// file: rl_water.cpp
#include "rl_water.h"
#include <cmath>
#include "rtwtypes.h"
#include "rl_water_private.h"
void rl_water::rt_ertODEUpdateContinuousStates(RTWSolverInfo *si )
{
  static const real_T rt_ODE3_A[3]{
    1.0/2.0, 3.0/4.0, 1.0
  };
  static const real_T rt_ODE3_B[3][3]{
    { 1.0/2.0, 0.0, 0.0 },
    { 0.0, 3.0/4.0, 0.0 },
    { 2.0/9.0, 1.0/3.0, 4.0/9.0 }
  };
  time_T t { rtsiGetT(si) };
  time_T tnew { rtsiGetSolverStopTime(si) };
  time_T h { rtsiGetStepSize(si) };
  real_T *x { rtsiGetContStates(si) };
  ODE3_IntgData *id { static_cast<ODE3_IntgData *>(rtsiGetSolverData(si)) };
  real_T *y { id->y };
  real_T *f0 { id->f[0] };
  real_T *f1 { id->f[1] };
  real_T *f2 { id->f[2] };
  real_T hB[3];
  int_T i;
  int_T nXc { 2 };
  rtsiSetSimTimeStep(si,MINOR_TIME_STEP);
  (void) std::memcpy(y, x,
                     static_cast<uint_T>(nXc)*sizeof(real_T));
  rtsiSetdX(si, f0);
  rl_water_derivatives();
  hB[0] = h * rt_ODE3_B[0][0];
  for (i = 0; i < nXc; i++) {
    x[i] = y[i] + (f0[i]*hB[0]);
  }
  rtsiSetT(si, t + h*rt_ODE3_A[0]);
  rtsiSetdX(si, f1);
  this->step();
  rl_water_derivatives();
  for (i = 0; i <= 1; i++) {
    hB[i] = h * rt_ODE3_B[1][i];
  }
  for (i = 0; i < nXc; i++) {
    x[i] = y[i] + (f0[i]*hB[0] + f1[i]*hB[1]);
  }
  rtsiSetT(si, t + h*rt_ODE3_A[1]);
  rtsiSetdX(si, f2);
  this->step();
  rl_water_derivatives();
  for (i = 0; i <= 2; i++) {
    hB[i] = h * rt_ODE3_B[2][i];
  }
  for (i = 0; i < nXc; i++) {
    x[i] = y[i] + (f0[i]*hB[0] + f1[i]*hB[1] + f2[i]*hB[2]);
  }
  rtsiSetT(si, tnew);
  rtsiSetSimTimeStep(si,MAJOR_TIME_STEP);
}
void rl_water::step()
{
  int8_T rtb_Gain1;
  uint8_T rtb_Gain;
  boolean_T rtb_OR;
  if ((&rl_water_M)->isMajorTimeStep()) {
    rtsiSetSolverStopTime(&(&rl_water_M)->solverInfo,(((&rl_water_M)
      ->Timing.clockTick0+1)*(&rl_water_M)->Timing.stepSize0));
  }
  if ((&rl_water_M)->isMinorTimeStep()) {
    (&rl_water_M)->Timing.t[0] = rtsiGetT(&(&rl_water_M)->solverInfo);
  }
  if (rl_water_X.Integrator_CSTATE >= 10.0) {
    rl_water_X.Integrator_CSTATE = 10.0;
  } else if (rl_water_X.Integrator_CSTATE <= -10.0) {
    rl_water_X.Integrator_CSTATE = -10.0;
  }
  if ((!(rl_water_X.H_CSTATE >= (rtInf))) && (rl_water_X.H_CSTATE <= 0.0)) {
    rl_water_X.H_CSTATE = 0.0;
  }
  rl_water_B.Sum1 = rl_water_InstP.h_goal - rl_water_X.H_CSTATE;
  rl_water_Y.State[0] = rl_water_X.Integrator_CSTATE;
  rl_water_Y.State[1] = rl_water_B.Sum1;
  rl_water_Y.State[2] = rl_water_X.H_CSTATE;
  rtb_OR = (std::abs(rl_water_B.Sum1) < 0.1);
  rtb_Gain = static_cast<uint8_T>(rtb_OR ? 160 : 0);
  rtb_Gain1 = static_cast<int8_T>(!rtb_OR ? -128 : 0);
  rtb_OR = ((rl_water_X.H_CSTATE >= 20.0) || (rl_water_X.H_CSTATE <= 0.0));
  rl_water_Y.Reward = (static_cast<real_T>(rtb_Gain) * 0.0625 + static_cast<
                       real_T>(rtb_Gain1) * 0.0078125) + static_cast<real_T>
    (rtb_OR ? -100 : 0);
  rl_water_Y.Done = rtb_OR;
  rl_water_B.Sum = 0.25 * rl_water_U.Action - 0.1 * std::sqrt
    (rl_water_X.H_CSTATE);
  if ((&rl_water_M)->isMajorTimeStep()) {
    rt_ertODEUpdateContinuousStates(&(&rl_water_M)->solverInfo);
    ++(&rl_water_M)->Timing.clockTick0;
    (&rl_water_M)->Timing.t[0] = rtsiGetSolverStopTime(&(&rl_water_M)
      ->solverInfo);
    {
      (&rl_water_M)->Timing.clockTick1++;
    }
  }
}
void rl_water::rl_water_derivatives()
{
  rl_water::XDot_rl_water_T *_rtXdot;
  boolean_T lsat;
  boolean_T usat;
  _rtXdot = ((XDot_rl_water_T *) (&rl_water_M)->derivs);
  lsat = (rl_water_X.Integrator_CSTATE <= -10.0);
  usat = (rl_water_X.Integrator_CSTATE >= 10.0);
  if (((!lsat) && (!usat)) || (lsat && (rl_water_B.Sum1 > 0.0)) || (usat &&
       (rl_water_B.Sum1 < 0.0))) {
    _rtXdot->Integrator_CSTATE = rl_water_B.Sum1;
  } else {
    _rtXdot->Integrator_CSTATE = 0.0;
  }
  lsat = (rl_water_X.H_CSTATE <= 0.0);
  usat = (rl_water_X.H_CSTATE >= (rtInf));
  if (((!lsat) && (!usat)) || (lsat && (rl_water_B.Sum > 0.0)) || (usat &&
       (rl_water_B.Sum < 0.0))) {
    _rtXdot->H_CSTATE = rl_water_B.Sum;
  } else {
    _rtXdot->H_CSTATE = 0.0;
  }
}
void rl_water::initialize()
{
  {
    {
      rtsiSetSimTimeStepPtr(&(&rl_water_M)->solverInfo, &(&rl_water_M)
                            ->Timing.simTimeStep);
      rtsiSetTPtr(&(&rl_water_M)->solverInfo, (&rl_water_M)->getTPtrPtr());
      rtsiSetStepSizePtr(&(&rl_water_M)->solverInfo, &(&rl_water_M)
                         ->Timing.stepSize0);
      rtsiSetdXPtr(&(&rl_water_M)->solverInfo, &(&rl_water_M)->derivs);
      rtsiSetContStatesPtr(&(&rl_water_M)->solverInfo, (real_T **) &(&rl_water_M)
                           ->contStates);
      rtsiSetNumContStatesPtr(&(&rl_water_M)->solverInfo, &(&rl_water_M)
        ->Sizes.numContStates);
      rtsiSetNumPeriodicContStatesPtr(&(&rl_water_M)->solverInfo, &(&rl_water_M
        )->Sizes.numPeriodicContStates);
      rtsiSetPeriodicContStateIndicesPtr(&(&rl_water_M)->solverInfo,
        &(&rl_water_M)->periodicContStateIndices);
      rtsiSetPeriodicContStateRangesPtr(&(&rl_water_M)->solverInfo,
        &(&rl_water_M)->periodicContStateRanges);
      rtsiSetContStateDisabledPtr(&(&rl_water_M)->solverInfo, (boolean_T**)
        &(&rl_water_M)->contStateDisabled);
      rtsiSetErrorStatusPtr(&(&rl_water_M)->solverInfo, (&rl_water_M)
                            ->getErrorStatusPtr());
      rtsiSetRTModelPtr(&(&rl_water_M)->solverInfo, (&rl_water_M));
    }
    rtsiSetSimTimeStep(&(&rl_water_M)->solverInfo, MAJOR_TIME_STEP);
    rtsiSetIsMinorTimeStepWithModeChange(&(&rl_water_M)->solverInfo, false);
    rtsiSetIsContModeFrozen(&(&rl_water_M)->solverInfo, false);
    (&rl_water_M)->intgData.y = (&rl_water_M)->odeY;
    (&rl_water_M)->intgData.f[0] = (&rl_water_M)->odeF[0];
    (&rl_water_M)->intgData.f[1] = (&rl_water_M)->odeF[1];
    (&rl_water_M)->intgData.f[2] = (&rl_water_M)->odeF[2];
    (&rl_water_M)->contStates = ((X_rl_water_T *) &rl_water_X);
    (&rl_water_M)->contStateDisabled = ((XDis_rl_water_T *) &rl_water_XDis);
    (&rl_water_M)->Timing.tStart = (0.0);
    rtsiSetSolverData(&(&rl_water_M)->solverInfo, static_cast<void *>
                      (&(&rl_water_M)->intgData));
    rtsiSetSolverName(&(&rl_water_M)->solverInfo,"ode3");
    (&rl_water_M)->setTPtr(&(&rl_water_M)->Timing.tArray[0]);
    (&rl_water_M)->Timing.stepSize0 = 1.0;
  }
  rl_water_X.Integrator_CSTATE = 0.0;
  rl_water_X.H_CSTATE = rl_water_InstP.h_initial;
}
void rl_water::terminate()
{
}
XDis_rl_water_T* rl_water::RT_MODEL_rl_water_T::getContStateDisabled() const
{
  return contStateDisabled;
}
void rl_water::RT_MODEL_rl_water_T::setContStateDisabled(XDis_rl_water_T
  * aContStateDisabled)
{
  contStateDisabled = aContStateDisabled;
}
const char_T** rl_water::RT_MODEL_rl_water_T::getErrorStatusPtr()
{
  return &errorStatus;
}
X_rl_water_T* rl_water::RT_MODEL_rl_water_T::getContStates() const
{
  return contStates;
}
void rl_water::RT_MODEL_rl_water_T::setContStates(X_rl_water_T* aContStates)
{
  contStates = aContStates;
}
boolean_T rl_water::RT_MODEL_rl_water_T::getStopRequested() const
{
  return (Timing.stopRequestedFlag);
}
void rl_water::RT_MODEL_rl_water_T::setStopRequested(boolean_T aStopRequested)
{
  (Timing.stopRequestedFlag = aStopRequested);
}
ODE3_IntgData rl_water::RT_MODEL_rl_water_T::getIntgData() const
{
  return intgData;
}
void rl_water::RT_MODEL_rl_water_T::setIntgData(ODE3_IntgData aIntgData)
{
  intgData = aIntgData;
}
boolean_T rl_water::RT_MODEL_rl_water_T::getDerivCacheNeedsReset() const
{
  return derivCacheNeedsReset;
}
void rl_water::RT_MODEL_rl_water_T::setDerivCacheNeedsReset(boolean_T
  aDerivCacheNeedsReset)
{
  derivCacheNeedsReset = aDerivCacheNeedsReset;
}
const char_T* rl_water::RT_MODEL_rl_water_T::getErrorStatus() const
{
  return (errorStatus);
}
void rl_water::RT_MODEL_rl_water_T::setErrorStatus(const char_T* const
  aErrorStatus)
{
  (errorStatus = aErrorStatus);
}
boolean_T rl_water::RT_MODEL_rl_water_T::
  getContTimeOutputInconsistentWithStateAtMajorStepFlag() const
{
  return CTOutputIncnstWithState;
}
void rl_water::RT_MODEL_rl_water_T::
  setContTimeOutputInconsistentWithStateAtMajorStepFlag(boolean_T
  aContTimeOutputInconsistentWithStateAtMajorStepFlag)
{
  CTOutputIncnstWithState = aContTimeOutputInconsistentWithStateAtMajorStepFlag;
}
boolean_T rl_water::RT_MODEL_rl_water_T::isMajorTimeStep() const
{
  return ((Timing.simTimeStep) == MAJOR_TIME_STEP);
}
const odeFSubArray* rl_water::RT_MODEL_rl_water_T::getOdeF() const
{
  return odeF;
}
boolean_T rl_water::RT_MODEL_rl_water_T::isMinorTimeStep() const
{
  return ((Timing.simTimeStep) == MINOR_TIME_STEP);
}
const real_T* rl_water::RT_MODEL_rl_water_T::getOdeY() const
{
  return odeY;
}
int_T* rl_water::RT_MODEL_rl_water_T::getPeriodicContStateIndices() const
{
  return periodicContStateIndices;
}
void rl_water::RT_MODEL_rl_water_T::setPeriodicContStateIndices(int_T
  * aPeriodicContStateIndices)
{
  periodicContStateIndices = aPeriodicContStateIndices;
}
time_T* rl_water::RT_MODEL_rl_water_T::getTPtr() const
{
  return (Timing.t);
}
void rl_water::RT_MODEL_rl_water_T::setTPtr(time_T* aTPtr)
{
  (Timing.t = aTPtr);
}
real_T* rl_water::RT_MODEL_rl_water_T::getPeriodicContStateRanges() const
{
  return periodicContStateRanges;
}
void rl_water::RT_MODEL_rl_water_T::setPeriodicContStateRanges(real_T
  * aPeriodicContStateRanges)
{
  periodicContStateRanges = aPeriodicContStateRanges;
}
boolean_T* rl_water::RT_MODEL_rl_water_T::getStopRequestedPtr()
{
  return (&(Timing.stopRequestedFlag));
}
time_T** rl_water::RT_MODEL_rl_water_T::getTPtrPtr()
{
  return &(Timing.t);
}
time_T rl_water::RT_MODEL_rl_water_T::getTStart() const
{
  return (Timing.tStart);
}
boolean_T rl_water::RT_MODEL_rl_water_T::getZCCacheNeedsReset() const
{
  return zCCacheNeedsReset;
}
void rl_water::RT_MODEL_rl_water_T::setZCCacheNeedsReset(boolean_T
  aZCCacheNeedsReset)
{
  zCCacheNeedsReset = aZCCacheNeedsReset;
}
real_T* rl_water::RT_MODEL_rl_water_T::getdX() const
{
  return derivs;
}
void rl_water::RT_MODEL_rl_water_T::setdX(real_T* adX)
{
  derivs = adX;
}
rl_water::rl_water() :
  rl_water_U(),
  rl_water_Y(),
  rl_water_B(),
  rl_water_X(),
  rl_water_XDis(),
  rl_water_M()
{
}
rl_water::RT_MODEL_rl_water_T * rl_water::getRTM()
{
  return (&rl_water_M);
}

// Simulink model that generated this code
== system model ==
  Action : Inport
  State : Outport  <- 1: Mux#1
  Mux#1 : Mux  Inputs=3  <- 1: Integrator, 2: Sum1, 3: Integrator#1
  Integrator : Integrator  LimitOutput=on  UpperSaturationLimit=10  LowerSaturationLimit=-10  <- 1: Sum1
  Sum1 : Sum  Inputs=+-  <- 1: Constant#1, 2: Integrator#1
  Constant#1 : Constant  Value=h_goal
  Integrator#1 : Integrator  InitialCondition=h_initial  LimitOutput=on  LowerSaturationLimit=0  <- 1: Sum
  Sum : Sum  Inputs=+-  <- 1: Gain#1, 2: Gain#2
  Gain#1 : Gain  Gain=0.25  <- 1: Action
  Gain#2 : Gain  Gain=0.1  <- 1: Sqrt#1
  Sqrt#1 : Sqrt  <- 1: Integrator#1
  Reward : Outport  <- 1: Sum#1
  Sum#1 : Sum  Inputs=+++  <- 1: Gain, 2: Gain1, 3: Gain#3
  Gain : Gain  Gain=10  <- 1: CompareToConstant#1
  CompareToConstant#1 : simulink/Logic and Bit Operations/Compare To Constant  relop=<  const=0.1  <- 1: Abs#1
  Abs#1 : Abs  <- 1: Sum1
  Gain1 : Gain  Gain=-1  <- 1: Logic#1
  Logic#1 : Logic  Operator=NOT  <- 1: CompareToConstant#1
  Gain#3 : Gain  Gain=-100  <- 1: OR
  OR : Logic  Operator=OR  <- 1: CompareToConstant#2, 2: CompareToZero#1
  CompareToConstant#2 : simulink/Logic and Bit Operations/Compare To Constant  relop=>=  const=20  <- 1: Integrator#1
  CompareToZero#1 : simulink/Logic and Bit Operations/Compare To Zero  relop=<=  <- 1: Integrator#1
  Done : Outport  <- 1: OR
